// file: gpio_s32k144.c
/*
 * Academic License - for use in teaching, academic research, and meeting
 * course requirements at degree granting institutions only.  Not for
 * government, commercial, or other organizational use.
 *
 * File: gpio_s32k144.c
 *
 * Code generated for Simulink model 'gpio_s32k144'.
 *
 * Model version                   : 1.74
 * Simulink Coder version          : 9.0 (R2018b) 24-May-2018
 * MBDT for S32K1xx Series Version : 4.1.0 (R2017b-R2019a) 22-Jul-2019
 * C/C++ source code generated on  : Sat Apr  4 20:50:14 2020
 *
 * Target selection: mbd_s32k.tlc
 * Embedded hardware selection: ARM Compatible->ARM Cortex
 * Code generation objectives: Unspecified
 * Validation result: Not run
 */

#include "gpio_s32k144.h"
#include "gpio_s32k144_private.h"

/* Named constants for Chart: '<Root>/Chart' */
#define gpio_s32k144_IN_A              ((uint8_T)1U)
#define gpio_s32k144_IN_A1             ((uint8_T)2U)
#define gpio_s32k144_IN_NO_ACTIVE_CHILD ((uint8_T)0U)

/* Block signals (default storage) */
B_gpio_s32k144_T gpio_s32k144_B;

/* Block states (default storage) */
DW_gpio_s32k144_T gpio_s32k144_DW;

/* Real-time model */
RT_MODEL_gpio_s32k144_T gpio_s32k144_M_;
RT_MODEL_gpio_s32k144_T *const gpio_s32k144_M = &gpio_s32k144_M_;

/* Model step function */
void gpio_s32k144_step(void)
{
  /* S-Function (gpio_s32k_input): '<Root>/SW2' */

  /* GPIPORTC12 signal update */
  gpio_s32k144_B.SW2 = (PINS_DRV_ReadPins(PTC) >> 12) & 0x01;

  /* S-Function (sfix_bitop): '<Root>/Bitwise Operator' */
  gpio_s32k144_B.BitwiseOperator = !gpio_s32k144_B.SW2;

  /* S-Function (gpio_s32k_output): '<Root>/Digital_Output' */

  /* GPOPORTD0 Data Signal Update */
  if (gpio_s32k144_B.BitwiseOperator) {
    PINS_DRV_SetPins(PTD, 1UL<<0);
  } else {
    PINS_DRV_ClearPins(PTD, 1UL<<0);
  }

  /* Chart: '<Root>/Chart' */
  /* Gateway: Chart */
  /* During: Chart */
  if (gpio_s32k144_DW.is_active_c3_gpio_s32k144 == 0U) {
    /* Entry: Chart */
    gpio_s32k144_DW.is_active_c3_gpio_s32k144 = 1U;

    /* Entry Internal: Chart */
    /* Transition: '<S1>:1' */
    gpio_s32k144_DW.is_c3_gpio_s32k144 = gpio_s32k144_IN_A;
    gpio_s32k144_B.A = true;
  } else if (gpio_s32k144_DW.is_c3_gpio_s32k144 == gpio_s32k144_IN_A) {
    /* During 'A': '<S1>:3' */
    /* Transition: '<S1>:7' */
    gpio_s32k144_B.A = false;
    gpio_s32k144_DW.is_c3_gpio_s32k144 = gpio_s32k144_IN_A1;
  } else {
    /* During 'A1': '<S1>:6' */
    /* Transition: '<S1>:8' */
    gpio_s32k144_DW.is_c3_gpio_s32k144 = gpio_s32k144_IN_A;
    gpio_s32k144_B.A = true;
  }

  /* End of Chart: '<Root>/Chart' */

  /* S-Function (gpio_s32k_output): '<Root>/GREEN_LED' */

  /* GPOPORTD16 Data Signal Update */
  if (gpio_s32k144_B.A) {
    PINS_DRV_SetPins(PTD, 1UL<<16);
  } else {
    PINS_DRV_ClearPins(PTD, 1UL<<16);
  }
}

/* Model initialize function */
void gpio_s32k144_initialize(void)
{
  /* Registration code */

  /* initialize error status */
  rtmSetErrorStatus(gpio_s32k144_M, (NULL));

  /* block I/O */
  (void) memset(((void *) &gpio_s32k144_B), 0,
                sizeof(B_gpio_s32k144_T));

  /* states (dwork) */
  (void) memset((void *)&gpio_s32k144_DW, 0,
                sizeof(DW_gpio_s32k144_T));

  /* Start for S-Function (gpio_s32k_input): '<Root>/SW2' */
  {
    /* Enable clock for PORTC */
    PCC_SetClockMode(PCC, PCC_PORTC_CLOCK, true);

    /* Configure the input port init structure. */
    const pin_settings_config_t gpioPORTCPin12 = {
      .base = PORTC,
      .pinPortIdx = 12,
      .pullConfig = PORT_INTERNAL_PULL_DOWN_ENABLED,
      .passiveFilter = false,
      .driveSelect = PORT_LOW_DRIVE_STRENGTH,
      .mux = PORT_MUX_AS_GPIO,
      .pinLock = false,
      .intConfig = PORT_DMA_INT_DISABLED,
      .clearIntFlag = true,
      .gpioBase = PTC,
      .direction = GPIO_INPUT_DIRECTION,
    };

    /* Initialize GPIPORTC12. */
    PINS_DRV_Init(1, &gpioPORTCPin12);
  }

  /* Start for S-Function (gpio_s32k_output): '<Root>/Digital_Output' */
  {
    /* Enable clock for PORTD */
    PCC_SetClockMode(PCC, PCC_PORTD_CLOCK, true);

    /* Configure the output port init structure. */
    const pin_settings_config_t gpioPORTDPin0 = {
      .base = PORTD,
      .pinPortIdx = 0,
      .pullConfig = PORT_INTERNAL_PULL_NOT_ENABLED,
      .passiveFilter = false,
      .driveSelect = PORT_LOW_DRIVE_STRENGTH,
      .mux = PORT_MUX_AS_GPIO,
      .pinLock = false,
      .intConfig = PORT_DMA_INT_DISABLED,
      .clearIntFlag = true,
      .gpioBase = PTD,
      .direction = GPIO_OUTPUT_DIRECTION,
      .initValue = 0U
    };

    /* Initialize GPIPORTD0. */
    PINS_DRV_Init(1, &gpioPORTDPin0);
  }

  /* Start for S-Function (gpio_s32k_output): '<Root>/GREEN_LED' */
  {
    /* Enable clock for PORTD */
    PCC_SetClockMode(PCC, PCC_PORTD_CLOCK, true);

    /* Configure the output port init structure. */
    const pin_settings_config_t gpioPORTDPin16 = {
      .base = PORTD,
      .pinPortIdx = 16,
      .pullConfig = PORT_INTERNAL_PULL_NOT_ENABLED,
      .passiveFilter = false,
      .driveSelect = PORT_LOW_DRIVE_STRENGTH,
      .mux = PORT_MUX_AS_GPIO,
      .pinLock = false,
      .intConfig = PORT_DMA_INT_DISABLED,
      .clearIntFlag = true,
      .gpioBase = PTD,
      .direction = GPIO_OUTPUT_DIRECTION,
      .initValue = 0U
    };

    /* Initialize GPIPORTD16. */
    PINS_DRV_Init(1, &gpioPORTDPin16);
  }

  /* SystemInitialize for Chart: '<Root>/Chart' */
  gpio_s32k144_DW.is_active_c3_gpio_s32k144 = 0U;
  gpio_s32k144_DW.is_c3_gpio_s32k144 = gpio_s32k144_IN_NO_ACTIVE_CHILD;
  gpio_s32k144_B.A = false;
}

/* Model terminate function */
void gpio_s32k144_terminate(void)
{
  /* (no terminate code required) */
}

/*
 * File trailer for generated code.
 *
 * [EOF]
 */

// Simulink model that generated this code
simulink model "gpio_s32k144"  (Simulink 9.2)
settings: Solver=FixedStepDiscrete  StartTime=0.0  StopTime=10.0  FixedStep=0.1  RelTol=1e-3  EnableMultiTasking=on
InitFcn:
  | mbd_s32k_consistency_checks(bdroot(gcs));
undefined symbols (not defined in the file): LQFP
libraries: mbd_s32k1xx_ec_toolbox x4, simulink x2

== system gpio_s32k144 ==
  Bitwise Operator : simulink/Logic and Bit Operations/Bitwise Operator  logicop=NOT  UseBitMask=off  BitMask=bin2dec('11011001')  BitMaskRealWorld=Stored Integer
  Chart : Stateflow chart  TreatAsAtomicUnit=on
  Digital_Output : mbd_s32k1xx_ec_toolbox/GPIO Blocks/Digital_Output  gpio_pin=PTD0: [PTD0 | Port D I/O]  init_val=Low  drive_strength=Low
  GREEN_LED : mbd_s32k1xx_ec_toolbox/GPIO Blocks/Digital_Output  gpio_pin=PTD16: [PTD16 | Port D I/O]  init_val=Low  drive_strength=Low
  MBD_S32K14x_Config_Information : mbd_s32k1xx_ec_toolbox/MBD_S32K1xx_Config_Information  mbdt_ver=0  disp_str=|  config_params=[]  mcu_target_name=S32K144  mcu_target_package=100-LQFP  mcu_target_sram_size=64KB  mcu_system_clock_freq=80  mcu_xtal_freq=External 8  mcu_steptick_timer=LPIT Channel 0  mcu_steptick_prio=15  ds_import_enable=on  target_compiler=GCC  target_memory=FLASH  gcc_target_compile_opts=-mcpu=cortex-m4 -mthumb -mfloat-abi=hard -mfpu=fpv4-sp-d16 -O1 -g -gstrict-dwarf  gcc_target_assemble_opts=-mcpu=cortex-m4 -mthumb -mfloat-abi=hard -mfpu=fpv4-sp-d16 -g  gcc_target_link_opts=-mcpu=cortex-m4 -mthumb -mfloat-abi=hard -mfpu=fpv4-sp-d16  gcc_target_default_lcf=on  gcc_target_user_lcf=S32K144_64_flash.ld  ghs_target_compile_opts=-cpu=cortexm4f -thumb -DARM_MATH_CM4 -fpu=vfpv4_d16 -fsingle -Ogeneral -Wundef -Wimplicit-int -Wshadow -Wtrigraphs --no_commons --gnu_asm -gnu99 -gdwarf-2 -G  ghs_target_assemble_opts=-cpu=cortexm4f -fpu=vfpv4_d16  ghs_target_link_opts=-cpu=cortexm4f -thumb -fpu=vfpv4_d16  ghs_target_default_lcf=on  ghs_target_user_lcf=S32K144_64_flash.ld  iar_target_compile_opts=--cpu=Cortex-M4F --thumb --fpu=VFPv4_sp -Ol -e --debug --dlib_config normal  iar_target_assemble_opts=--cpu Cortex-M4F --thumb --fpu VFPv4_sp  iar_target_link_opts=--no_exceptions --vfe --inline  iar_target_default_lcf=on  iar_target_user_lcf=S32K144_64_flash.icf  pil_download_enable=off  rbl_download_enable=on  rbl_start_delay=5000000  rbl_download_interface=OpenSDA  rbl_restart_request=off  rbl_com_port=Custom  rbl_com_port_custom=COM1  pil_download_rate=57600  pil_opensda_drive=D: EVB-S32K144  pil_opensda_drive_custom=D  pil_uart_instance=1  pil_uart_rx=PTC6: [LPUART1_RX | Receive]  pil_uart_tx=PTC7: [LPUART1_TX | Transmit]  FTM_PWM_PcrCheckEnDis=on  FTM_Input_Edge_Inputs_PcrCheckEnDis=on  FTM_Dual_Edge_Inputs_PcrCheckEnDis=on  FTM_Quadrature_Inputs_PcrCheckEnDis=on  FTM_Hall_Sensor_Inputs_PcrCheckEnDis=on  LPTMR_PcrCheckEnDis=on  PIT_PcrCheckEnDis=on  RTC_PcrCheckEnDis=on  FlexCAN_PcrCheckEnDis=on  LIN_PcrCheckEnDis=on  FlexIO_PcrCheckEnDis=on  LPI2C_PcrCheckEnDis=on  LPSPI_PcrCheckEnDis=on  LPUART_PcrCheckEnDis=on  CMP_PcrCheckEnDis=on  GPIO_OutputPcrCheckEnDis=on  GPIO_InputPcrCheckEnDis=on  SBC_PcrCheckEnDis=on  AMMCLIB_PcrCheckEnDis=on  FM_PcrCheckEnDis=on  Profile_PcrCheckEnDis=on  ConfigParams_PcrCheckEnDis=on  ModelRef_PcrCheckEnDis=on  PDB0_PcrCheckEnDis=on  CSEc_PcrCheckEnDis=on  eDMA_PcrCheckEnDis=on  ADC_PcrCheckEnDis=on  WDOG_PcrCheckEnDis=on
      | Target : S32K144-64KB_SRAM
      | Package : 100-pin
      | System clock : 80 MHz
      | XTAL clock : External 8 MHz
      | Compiler : IAR
      | Target Type : FLASH
      | Download Code after build : off
      | Step Tick Interrupt Priority : 15
  Model Info : simulink/Model-Wide Utilities/Model Info  Frame=off  DisplayStringWithTags=|  HorizontalTextAlignment=Left  LeftAlignmentValue=0.02
      | Model Name: %<ModelName>
      | 
      | Description: %<Description>
  SW2 : mbd_s32k1xx_ec_toolbox/GPIO Blocks/Digital_Input  gpio_pin=PTC12: [PTC12 | Port C I/O]  pull_resistor=Pulldown  passive_filter=off
  wires:
  Chart/1(" A") -> GREEN_LED/1
  SW2/1 -> Bitwise Operator/1
  Bitwise Operator/1 -> Digital_Output/1

== stateflow chart Chart ==
  state A
  state A1
  (default) -> A
  A -> A1
  A1 -> A
  data: A output boolean [0..1]
